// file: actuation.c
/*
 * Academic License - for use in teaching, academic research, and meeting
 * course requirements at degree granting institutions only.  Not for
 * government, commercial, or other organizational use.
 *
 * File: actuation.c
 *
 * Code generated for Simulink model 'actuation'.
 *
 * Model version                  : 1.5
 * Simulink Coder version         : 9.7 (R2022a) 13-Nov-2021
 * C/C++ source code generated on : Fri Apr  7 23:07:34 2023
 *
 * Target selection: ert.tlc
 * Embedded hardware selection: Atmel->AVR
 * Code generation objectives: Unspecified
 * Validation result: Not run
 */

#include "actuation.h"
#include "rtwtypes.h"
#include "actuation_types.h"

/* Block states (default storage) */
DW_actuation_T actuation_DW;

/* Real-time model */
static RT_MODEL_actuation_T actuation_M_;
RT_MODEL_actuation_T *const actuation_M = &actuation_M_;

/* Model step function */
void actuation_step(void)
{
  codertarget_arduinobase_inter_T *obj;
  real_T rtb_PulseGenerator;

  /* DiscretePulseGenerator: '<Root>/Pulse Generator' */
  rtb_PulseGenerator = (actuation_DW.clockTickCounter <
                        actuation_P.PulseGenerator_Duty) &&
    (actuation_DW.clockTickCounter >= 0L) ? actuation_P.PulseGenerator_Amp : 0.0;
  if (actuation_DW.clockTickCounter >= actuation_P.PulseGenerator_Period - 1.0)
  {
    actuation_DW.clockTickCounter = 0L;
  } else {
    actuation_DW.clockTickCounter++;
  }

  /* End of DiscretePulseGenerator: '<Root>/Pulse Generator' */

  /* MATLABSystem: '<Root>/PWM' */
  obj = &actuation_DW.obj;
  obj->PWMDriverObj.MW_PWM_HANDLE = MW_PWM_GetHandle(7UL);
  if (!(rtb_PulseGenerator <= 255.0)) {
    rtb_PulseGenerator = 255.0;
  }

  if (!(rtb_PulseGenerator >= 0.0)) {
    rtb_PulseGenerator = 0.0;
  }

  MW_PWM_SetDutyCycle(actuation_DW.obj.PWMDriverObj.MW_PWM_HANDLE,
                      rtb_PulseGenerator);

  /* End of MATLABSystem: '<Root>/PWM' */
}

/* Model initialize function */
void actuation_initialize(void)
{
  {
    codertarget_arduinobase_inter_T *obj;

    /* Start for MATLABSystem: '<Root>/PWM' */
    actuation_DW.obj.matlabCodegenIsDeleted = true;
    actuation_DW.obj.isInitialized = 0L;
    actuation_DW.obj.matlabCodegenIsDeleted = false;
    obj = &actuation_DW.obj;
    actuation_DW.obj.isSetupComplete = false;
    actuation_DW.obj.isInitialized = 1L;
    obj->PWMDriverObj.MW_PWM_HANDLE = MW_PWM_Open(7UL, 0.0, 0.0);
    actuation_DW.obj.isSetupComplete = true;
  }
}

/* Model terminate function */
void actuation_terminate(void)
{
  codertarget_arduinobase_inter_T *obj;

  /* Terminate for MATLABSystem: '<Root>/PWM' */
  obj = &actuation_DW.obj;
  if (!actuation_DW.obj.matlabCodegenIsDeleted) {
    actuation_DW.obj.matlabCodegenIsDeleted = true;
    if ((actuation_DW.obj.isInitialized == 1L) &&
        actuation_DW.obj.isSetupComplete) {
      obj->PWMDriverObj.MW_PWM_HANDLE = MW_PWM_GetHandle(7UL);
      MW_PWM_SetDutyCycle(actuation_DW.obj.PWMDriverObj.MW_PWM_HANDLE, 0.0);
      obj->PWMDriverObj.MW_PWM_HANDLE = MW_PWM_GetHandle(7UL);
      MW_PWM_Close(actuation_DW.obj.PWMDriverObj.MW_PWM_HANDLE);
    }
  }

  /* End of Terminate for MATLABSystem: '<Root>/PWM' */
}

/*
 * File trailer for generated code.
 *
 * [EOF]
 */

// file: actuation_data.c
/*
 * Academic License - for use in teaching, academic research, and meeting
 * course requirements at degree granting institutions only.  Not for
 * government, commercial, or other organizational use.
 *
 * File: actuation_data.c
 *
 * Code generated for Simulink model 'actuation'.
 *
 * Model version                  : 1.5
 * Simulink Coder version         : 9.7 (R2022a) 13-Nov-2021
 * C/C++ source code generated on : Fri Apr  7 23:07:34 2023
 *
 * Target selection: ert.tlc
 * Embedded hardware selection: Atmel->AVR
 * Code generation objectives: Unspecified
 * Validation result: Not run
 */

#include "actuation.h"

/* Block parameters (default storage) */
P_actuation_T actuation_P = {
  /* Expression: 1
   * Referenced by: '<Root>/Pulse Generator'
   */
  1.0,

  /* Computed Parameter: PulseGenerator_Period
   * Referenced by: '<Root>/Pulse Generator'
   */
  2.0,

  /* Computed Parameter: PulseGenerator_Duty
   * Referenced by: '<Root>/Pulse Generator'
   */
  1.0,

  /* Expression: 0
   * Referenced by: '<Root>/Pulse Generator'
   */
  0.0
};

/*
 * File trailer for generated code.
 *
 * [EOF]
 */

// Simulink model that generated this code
simulink model "actuation"  (R2022a)
settings: Solver=FixedStepAuto  StartTime=0.0  StopTime=10.0  RelTol=1e-3
libraries: arduinolib x4, simulink x3

== system actuation ==
  Desired Shaft Angle : simulink/Sources/Repeating Sequence Stair  Commented=on  OutValues=[0:180 179:-1:1]  tsamp=0.01  OutMin=[]  OutMax=[]  OutDataTypeStr=uint8  OutputDataTypeScalingMode=uint8  OutDataType=fixdt(0,8)  ConRadixGroup=Best Precision: Vector-wise  OutScaling=2^-12
  Desired Shaft Angle1 : simulink/Sources/Repeating Sequence Stair  Commented=on  OutValues=[0:90 90:-1:1]  tsamp=0.01  OutMin=[]  OutMax=[]  OutDataTypeStr=uint8  OutputDataTypeScalingMode=uint8  OutDataType=fixdt(0,8)  ConRadixGroup=Best Precision: Vector-wise  OutScaling=2^-12
  Desired Shaft Angle3 : simulink/Sources/Repeating Sequence Stair  Commented=on  OutValues=[45:90 90:-1:1 1:45]  tsamp=0.01  OutMin=[]  OutMax=[]  OutDataTypeStr=uint8  OutputDataTypeScalingMode=uint8  OutDataType=fixdt(0,8)  ConRadixGroup=Best Precision: Vector-wise  OutScaling=2^-12
  PWM : arduinolib/PWM  pinNumber=7  frequencyType=Default  desiredFrequency=490.2  achievableFrequency=490.2
  Pulse Generator : DiscretePulseGenerator  PulseType=Time based  Period=0.001  PulseWidth=50
  Standard Servo Write : arduinolib/Standard Servo Write  Commented=on  pinNumber=3  ServoIndex=0  blockPlatform=arduino
  Standard Servo Write1 : arduinolib/Standard Servo Write  Commented=on  pinNumber=7  ServoIndex=1  blockPlatform=arduino
  Standard Servo Write3 : arduinolib/Standard Servo Write  Commented=on  pinNumber=5  ServoIndex=2  blockPlatform=arduino
  wires:
  Desired Shaft Angle/1 -> Standard Servo Write/1
  Desired Shaft Angle1/1 -> Standard Servo Write1/1
  Pulse Generator/1 -> PWM/1
  Desired Shaft Angle3/1 -> Standard Servo Write3/1
